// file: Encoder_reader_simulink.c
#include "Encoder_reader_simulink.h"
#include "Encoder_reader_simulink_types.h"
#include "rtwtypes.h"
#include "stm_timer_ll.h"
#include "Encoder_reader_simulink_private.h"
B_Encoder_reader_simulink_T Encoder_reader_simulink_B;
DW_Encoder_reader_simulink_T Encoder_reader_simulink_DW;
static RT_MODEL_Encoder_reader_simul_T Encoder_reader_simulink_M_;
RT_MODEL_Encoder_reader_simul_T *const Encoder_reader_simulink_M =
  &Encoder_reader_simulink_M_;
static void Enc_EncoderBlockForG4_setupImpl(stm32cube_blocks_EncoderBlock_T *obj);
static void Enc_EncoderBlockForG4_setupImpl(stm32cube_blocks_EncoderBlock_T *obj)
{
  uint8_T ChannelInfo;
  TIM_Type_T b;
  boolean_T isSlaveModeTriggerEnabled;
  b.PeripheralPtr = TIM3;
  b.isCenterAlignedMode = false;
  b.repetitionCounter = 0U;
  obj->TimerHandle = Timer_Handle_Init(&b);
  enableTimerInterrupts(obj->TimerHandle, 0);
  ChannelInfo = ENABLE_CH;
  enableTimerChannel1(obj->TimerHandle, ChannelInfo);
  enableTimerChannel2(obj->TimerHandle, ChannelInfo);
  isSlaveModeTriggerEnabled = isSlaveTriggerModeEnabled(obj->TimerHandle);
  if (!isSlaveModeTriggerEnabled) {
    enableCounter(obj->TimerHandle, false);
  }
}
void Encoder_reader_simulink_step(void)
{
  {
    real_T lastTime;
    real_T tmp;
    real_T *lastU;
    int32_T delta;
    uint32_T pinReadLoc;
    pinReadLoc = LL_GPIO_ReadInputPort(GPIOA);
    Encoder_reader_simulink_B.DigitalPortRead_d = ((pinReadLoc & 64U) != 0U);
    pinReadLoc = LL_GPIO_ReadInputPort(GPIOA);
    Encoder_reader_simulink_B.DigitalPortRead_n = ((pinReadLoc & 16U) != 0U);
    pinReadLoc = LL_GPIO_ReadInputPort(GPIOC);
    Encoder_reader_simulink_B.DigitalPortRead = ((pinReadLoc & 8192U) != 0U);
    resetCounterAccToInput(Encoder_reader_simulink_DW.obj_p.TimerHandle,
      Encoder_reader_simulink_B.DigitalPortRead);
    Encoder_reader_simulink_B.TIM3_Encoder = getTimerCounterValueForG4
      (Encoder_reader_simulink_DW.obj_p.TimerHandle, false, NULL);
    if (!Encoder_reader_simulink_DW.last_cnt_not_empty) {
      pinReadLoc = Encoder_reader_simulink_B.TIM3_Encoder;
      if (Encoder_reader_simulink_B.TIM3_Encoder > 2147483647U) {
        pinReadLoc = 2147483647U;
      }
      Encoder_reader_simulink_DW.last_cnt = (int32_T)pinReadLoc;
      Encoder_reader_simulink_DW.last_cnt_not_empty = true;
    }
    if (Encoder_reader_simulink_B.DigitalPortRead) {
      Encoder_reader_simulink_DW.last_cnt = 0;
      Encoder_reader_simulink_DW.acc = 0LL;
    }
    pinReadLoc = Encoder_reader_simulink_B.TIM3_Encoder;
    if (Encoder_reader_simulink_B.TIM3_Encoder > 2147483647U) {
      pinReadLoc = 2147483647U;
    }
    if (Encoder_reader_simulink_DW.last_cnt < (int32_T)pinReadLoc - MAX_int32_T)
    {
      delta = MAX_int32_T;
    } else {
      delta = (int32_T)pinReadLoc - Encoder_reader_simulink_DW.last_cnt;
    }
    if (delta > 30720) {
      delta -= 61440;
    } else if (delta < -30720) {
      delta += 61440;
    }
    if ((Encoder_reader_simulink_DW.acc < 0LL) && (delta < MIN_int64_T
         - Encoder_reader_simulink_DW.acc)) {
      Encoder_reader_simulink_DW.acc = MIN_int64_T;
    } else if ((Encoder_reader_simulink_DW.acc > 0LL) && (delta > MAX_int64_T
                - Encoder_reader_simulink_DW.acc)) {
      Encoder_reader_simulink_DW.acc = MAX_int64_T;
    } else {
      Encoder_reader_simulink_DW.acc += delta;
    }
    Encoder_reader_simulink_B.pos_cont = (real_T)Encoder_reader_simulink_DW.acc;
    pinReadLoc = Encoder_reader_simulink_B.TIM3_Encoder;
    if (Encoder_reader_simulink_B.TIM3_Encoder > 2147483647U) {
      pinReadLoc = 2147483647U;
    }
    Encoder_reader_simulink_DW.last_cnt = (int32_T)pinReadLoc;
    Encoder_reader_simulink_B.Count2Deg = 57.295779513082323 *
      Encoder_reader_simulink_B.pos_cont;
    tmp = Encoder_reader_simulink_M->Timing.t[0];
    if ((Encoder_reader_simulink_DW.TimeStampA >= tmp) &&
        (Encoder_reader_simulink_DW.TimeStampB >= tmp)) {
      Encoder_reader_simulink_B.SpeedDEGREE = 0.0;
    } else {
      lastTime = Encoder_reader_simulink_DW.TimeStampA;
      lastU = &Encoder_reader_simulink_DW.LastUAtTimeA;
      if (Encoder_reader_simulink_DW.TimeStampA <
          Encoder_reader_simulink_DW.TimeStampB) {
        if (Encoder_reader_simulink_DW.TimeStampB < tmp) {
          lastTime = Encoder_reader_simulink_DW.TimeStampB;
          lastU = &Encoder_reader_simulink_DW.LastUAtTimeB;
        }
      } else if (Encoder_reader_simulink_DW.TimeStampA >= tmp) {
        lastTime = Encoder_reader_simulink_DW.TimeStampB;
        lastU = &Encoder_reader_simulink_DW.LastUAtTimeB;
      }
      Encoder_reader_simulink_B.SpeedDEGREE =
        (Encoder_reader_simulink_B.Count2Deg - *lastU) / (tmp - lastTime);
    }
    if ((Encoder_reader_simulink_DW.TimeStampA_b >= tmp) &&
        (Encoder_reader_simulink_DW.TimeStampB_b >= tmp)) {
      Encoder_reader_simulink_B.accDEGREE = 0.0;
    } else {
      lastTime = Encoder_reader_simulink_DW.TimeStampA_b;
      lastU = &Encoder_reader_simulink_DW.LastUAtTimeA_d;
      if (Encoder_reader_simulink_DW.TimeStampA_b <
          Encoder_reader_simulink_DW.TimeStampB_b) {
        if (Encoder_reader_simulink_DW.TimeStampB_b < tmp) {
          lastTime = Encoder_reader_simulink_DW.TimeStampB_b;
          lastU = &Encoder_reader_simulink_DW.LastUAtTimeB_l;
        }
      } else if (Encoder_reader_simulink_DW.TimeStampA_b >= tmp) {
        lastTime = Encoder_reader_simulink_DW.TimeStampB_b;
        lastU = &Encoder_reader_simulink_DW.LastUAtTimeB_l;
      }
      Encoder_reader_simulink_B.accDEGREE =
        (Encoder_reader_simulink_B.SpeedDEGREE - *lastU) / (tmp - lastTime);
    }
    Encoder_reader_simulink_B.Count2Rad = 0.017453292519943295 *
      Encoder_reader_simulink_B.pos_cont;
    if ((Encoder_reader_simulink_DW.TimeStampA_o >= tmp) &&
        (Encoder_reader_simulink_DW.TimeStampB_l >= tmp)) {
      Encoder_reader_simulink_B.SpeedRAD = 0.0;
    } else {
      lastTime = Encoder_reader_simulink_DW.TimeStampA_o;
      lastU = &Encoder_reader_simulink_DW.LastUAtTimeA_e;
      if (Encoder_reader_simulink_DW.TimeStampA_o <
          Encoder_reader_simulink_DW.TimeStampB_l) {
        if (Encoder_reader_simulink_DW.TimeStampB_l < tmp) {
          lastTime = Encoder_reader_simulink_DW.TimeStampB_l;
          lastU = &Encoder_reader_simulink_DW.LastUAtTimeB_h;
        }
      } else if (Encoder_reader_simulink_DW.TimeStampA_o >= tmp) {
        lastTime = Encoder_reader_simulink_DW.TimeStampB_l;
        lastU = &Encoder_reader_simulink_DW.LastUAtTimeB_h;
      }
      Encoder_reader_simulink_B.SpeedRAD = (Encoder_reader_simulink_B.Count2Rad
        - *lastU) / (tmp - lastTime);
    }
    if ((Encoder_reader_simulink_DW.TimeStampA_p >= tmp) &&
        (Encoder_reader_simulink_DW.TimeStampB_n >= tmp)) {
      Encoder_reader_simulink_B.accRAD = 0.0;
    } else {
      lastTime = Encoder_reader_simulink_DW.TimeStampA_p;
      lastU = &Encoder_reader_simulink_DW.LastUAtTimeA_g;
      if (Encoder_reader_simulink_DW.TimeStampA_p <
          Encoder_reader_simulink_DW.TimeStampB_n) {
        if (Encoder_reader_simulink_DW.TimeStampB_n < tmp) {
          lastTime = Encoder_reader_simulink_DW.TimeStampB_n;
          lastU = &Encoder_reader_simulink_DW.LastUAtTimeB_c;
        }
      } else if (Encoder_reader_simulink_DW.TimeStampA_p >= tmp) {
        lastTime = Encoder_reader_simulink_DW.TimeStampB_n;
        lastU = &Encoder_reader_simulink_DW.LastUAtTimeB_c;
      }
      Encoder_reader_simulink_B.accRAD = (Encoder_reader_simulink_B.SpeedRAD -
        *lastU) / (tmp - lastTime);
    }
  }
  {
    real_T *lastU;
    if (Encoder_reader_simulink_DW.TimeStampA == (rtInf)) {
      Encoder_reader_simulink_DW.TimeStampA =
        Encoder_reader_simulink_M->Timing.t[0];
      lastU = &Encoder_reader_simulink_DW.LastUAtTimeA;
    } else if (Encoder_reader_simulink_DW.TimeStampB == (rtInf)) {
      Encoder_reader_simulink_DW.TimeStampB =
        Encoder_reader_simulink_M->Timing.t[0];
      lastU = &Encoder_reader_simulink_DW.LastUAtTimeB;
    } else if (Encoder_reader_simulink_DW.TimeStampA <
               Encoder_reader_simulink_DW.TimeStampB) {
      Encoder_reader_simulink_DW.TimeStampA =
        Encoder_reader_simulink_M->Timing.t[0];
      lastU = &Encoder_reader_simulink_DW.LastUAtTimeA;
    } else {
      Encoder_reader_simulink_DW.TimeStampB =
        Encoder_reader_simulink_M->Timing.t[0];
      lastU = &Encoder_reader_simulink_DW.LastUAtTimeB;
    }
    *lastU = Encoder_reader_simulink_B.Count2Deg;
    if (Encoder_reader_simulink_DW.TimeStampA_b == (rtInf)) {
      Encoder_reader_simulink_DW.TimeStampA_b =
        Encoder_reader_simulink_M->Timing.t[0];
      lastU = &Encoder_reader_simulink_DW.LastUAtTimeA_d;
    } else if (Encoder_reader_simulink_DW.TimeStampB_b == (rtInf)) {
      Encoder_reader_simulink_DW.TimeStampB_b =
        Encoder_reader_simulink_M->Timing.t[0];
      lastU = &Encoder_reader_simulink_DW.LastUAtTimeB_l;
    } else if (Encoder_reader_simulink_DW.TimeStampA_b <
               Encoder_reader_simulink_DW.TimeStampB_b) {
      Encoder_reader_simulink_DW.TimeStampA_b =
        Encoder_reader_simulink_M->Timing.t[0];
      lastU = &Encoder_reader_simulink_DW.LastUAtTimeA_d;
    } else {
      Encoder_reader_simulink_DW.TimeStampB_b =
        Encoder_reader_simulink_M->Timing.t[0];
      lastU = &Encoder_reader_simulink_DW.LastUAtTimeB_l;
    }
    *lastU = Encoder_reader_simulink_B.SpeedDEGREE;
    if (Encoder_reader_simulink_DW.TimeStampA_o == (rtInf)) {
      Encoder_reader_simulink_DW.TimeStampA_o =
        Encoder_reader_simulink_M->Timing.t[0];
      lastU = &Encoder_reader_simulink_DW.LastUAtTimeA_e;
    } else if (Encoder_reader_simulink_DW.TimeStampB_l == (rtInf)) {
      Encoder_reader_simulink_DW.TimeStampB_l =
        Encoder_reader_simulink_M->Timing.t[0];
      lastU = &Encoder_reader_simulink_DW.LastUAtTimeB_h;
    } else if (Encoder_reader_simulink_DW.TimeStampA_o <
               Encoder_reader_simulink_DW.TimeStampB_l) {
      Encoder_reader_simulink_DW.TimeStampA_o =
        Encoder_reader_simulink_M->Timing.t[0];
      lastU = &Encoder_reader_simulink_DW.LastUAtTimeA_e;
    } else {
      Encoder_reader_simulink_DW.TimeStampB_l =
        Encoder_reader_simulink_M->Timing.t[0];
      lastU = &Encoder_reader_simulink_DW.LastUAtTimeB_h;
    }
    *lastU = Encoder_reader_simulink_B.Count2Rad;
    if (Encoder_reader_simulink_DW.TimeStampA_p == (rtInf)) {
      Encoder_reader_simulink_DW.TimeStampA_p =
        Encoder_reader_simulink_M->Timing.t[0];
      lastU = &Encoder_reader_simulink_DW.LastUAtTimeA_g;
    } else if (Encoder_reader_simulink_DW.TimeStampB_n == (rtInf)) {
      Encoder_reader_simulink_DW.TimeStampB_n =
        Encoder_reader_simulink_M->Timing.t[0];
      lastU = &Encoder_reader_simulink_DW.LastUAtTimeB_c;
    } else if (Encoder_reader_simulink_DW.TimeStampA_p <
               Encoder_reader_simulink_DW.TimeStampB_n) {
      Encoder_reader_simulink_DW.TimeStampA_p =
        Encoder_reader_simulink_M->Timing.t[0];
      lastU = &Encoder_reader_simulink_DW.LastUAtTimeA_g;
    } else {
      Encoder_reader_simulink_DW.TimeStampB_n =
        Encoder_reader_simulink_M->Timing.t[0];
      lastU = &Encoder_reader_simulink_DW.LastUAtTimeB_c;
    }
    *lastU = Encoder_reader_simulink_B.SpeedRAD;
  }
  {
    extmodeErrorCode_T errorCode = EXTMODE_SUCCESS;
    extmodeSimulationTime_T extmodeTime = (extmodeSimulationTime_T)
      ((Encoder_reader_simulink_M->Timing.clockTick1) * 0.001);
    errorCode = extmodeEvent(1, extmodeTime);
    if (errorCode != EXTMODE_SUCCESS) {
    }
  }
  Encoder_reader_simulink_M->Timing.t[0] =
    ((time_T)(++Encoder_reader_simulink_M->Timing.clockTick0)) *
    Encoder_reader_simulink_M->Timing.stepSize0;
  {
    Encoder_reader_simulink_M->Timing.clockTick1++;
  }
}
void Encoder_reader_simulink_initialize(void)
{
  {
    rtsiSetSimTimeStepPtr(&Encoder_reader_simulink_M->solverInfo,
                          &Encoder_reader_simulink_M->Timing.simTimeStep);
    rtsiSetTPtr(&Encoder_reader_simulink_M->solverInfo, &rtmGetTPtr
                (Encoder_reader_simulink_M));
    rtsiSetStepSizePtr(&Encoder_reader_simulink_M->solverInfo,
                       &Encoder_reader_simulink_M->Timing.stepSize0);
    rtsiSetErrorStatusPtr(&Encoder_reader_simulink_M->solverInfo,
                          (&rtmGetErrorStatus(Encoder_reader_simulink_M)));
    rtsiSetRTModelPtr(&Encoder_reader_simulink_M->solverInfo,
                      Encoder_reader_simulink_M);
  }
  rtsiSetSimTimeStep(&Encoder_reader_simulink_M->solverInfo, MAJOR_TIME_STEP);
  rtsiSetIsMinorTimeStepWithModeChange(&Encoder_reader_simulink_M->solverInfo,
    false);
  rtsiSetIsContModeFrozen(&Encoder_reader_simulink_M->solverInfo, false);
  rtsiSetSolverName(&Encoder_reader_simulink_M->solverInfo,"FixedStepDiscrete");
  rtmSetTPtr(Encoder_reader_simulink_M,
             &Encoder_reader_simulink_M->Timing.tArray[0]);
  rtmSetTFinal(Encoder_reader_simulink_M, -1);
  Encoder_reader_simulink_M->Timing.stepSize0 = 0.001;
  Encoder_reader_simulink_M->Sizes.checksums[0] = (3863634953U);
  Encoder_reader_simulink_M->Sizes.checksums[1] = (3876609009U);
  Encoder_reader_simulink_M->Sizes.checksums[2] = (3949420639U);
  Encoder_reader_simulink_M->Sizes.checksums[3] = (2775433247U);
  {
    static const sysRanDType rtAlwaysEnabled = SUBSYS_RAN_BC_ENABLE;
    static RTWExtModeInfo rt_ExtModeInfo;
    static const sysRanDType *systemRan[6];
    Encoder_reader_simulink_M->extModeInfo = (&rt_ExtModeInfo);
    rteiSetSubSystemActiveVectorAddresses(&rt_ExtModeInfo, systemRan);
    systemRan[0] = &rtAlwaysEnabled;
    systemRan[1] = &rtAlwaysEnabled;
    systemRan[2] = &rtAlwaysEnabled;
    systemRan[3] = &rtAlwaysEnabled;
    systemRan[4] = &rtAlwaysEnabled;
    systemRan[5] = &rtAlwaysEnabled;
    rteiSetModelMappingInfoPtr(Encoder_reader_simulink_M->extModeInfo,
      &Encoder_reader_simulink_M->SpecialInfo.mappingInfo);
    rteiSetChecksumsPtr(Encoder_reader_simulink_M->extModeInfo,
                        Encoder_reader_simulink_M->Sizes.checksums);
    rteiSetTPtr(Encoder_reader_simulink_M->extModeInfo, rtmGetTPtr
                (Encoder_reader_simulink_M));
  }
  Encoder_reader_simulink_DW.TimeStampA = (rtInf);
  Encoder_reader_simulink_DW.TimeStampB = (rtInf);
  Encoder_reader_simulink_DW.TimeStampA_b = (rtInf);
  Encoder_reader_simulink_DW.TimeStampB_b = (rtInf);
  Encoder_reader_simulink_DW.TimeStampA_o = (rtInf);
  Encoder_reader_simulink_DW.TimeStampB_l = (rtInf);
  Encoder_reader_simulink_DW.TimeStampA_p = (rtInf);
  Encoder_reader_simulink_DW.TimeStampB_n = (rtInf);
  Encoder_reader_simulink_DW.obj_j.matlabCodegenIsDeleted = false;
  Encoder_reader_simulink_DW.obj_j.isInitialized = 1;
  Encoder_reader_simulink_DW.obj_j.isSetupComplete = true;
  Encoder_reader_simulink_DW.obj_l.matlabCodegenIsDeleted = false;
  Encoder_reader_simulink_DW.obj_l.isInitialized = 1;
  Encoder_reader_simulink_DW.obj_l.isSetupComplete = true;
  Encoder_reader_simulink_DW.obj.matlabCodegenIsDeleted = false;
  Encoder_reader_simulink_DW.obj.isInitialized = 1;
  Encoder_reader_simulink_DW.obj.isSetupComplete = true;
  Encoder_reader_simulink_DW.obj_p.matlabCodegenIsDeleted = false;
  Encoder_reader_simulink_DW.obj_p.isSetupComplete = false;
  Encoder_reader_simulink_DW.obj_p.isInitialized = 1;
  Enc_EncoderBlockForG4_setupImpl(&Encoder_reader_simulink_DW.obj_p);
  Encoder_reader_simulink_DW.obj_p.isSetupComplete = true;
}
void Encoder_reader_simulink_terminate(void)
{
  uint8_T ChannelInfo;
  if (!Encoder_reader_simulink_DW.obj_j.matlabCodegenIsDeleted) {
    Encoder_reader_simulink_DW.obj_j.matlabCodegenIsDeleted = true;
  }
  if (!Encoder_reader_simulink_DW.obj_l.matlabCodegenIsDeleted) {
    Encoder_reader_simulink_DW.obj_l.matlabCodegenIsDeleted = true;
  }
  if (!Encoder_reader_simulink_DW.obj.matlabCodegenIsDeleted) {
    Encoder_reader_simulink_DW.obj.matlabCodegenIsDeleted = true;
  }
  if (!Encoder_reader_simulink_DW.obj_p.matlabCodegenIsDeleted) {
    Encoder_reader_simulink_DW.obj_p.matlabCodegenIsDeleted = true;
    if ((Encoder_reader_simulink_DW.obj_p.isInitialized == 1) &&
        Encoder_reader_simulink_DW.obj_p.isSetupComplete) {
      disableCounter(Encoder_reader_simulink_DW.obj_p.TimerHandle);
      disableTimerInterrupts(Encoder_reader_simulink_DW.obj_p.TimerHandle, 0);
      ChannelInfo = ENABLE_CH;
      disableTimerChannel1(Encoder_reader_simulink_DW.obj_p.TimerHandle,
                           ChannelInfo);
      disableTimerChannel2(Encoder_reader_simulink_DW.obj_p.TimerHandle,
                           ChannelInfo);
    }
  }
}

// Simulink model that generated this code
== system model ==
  accDEGREE : Derivative  <- 1: SpeedDEGREE
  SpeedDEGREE : Derivative  <- 1: Count2Deg
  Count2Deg : Gain  Gain=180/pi  <- 1: MATLABFunction#1
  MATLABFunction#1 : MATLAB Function  <- 1: DigitalPortRead#1, 2: DataTypeConversion#1
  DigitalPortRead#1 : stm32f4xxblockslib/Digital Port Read
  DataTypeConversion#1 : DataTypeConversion  <- 1: TIM3_Encoder
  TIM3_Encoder : stm32g4xxblockslib/Encoder  <- 1: DigitalPortRead#1
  accRAD : Derivative  <- 1: SpeedRAD
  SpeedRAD : Derivative  <- 1: Count2Rad
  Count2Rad : Gain  Gain=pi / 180  <- 1: MATLABFunction#1
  DigitalPortRead#2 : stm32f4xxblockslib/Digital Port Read
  DigitalPortRead#3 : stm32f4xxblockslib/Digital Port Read
== matlab function MATLABFunction#1 ==
function pos_cont = WrapAround(data,cnt)
persistent last_cnt acc
if isempty(last_cnt)
    last_cnt = int32(cnt);
    acc = int64(0);
end
%homing sequence for wrap around
if data == 1
    last_cnt = int32(0);
    acc = int64(0);
end

MAX_COUNT = int32(61439);
RANGE = int32(MAX_COUNT) + int32(1);   % 61440
HALF = RANGE/2;

delta = int32(cnt) - last_cnt;

% detect wrap
if delta > HALF
    delta = delta - RANGE;   % clockwise large positive -> negative jump (wrap backward)
elseif delta < -HALF
    delta = delta + RANGE;   % counterclockwise large negative -> positive jump (wrap forward)
end

acc = acc + int64(delta);   % accumulate corrected change
pos_cont = double(acc);
last_cnt = int32(cnt);
end
